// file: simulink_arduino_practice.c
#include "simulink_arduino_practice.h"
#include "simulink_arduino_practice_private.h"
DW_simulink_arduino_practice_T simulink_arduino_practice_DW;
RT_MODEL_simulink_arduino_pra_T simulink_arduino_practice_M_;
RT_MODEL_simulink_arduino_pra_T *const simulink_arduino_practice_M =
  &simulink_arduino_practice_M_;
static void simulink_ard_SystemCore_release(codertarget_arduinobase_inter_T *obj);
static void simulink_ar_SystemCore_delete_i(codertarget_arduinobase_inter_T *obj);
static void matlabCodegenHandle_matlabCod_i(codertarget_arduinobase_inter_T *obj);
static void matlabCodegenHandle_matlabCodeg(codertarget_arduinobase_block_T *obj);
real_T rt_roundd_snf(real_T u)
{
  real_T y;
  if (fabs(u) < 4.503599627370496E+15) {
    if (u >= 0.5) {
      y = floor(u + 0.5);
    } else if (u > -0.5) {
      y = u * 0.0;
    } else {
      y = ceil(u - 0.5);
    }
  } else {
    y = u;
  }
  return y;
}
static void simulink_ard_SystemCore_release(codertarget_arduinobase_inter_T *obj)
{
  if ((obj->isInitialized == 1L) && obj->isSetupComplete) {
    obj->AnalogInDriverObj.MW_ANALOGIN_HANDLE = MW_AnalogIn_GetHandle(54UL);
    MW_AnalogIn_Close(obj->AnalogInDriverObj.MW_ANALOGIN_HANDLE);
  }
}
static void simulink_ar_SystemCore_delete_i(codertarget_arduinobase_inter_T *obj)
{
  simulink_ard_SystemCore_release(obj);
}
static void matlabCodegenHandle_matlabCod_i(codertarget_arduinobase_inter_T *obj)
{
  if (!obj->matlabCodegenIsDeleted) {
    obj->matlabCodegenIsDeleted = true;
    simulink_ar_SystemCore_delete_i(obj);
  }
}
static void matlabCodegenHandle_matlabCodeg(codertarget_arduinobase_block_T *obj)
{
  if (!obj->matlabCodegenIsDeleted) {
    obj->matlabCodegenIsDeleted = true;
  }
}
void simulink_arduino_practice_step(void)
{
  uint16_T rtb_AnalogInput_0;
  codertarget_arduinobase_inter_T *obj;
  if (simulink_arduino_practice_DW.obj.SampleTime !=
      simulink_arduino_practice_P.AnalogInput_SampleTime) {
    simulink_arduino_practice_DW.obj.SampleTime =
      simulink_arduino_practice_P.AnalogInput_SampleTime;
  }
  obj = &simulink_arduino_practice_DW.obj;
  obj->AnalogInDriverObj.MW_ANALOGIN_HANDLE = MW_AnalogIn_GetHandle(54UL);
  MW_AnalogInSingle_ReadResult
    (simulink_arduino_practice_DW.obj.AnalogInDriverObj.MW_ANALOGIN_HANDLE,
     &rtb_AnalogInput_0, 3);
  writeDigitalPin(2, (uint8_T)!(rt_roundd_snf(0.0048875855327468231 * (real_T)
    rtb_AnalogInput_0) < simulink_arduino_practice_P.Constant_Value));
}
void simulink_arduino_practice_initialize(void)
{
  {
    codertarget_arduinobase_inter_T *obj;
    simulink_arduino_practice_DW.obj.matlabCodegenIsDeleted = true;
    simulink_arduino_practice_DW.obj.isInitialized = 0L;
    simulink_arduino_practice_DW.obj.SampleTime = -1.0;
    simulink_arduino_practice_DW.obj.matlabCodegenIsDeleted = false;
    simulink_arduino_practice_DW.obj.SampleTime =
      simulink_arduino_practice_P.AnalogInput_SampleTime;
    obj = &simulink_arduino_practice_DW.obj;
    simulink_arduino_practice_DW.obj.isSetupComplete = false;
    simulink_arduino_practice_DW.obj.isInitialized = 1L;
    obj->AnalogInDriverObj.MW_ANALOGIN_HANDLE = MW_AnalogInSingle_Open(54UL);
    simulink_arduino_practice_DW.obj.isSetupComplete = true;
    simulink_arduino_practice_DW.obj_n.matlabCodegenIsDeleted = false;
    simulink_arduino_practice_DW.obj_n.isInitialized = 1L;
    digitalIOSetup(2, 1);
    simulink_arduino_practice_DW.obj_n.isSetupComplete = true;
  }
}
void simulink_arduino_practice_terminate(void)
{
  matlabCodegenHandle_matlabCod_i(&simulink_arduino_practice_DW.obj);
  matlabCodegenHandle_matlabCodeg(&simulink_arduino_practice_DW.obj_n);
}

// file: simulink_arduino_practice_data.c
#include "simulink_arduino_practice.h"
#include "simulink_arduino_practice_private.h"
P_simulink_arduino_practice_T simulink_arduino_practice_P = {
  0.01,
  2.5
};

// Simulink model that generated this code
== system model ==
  DigitalOutput#1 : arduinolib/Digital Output  pinNumber=2  <- 1: MATLABFunction#1
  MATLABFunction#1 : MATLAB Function  <- 1: AnalogInput, 2: Constant
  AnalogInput : arduinolib/Analog Input  pinNumber=0
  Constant : Constant  Value=2.5
== matlab function MATLABFunction#1 ==
function y = fcn(voltage,threshold)
bins = 1023;
ref_v = 5;
voltage = ref_v/bins * voltage;
if voltage < threshold
            out = 0;
        else
            out = 1;
        end
y = out;
